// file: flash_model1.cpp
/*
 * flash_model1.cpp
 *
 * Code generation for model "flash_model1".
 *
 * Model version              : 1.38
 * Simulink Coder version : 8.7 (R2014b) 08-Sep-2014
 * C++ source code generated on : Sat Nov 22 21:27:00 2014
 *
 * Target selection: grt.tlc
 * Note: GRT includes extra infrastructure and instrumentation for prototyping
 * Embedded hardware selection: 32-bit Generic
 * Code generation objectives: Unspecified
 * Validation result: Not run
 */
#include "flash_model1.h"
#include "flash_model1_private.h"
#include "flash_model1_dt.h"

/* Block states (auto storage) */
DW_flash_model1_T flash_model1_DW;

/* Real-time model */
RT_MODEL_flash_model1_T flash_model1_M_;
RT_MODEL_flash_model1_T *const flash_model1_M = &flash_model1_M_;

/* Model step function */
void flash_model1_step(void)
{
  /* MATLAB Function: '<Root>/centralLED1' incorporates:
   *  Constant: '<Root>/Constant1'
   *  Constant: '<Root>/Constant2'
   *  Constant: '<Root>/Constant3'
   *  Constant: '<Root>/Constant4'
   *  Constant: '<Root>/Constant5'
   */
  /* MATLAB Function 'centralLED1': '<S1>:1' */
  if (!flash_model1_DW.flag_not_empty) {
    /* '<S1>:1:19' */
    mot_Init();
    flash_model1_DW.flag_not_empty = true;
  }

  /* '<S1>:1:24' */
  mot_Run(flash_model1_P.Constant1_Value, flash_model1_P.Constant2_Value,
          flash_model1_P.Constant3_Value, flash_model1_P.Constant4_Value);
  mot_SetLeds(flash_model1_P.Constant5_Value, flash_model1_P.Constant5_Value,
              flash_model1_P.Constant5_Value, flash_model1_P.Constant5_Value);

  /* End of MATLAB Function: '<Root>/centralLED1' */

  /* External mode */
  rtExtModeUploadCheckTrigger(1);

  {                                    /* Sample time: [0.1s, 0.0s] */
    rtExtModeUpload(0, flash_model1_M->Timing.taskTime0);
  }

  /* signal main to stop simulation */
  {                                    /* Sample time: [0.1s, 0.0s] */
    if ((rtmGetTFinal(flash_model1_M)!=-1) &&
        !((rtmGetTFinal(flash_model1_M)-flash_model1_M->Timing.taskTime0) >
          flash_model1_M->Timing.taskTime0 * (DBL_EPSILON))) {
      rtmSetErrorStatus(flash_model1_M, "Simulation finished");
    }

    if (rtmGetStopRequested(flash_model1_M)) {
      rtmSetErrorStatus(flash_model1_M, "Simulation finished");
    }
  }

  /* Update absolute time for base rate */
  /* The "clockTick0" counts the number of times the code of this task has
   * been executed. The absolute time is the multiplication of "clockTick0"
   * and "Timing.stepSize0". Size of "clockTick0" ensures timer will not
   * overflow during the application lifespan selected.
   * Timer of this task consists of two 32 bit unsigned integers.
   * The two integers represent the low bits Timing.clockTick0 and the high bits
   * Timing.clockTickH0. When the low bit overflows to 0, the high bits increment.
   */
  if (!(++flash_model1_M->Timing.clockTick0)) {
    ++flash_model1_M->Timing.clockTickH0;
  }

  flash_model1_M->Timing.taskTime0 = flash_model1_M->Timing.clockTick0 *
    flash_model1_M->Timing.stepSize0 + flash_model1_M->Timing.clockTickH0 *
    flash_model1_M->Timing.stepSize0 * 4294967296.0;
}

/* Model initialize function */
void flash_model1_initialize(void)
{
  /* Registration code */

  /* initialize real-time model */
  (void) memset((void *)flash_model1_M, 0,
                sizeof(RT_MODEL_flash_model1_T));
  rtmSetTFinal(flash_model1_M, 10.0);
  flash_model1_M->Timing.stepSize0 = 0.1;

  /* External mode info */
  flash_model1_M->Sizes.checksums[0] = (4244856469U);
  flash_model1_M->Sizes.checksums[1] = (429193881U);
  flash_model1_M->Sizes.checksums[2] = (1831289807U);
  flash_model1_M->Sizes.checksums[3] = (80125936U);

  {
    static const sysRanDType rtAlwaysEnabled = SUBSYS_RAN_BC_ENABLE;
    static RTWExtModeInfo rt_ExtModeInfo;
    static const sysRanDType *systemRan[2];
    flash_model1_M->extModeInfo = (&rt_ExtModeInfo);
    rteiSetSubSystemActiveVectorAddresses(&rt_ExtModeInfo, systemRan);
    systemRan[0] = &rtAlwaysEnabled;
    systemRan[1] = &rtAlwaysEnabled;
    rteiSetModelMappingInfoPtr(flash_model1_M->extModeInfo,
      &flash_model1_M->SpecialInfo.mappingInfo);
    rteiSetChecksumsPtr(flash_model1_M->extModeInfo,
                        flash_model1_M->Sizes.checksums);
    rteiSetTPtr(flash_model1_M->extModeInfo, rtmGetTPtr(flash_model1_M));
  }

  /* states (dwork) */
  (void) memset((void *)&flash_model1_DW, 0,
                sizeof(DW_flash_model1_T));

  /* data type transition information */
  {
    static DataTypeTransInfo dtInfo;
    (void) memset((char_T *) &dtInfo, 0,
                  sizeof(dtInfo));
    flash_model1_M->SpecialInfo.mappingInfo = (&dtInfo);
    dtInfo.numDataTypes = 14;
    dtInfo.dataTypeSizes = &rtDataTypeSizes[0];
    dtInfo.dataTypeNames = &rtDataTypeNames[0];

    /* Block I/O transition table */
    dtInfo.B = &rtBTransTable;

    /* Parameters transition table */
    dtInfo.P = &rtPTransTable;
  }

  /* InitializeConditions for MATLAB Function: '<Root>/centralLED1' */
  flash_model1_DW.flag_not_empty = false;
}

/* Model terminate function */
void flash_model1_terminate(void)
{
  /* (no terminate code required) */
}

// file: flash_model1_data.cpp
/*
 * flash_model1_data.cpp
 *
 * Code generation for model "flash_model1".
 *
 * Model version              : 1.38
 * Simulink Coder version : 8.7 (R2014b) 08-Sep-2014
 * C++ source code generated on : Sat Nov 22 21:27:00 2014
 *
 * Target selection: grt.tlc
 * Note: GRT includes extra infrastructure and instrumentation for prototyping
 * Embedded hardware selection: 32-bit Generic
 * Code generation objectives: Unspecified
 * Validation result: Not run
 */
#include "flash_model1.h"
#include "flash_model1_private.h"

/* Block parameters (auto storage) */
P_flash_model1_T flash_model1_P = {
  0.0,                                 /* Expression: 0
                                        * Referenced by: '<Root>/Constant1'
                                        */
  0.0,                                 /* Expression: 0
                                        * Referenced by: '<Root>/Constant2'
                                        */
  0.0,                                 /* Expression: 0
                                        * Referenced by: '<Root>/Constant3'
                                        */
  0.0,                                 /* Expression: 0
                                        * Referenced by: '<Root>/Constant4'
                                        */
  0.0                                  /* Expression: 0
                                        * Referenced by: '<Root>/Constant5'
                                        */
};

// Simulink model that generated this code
simulink model "flash_model1"  (R2014b)
settings: Solver=FixedStepDiscrete  SolverMode=SingleTasking  StartTime=0.0  StopTime=10.0  FixedStep=.1  RelTol=1e-3

== system flash_model1 ==
  Constant1 : Constant  Value=0
  Constant2 : Constant  Value=0
  Constant3 : Constant  Value=0
  Constant4 : Constant  Value=.01
  Constant5 : Constant  Value=3
  centralLED1 : MATLAB Function  TreatAsAtomicUnit=on
  wires:
  Constant1/1 -> centralLED1/1(motor1)
  Constant2/1 -> centralLED1/2(motor2)
  Constant3/1 -> centralLED1/3(motor3)
  Constant4/1 -> centralLED1/4(motor4)
  Constant5/1 -> centralLED1/5(led)

== matlab function flash_model1/centralLED1 ==
function motorController(motor1,motor2,motor3,motor4,led)
%#codegen

persistent flag

coder.cinclude('/Users/aodell/Documents/MATLAB/test_sim/mycfiles/mot.h');
coder.cinclude('/Users/aodell/Documents/MATLAB/test_sim/mycfiles/motorboard.h');
coder.cinclude('/Users/aodell/Documents/MATLAB/test_sim/mycfiles/util.h');
coder.cinclude('/Users/aodell/Documents/MATLAB/test_sim/mycfiles/gpio.h');

switch coder.target

    % Define how the block behaves in simulation mode 
    case 'sfun' 

    % Define how the block behaves in real time execution 
    case 'rtw'
        
        if isempty(flag),
            coder.ceval('mot_Init');
            flag=1;
        end;
        
        motorArr= double([motor1,motor2,motor3,motor4]);
        coder.ceval('mot_Run',motorArr(1),motorArr(2),motorArr(3),motorArr(4));
        coder.ceval('mot_SetLeds',led,led,led,led);
        
end
